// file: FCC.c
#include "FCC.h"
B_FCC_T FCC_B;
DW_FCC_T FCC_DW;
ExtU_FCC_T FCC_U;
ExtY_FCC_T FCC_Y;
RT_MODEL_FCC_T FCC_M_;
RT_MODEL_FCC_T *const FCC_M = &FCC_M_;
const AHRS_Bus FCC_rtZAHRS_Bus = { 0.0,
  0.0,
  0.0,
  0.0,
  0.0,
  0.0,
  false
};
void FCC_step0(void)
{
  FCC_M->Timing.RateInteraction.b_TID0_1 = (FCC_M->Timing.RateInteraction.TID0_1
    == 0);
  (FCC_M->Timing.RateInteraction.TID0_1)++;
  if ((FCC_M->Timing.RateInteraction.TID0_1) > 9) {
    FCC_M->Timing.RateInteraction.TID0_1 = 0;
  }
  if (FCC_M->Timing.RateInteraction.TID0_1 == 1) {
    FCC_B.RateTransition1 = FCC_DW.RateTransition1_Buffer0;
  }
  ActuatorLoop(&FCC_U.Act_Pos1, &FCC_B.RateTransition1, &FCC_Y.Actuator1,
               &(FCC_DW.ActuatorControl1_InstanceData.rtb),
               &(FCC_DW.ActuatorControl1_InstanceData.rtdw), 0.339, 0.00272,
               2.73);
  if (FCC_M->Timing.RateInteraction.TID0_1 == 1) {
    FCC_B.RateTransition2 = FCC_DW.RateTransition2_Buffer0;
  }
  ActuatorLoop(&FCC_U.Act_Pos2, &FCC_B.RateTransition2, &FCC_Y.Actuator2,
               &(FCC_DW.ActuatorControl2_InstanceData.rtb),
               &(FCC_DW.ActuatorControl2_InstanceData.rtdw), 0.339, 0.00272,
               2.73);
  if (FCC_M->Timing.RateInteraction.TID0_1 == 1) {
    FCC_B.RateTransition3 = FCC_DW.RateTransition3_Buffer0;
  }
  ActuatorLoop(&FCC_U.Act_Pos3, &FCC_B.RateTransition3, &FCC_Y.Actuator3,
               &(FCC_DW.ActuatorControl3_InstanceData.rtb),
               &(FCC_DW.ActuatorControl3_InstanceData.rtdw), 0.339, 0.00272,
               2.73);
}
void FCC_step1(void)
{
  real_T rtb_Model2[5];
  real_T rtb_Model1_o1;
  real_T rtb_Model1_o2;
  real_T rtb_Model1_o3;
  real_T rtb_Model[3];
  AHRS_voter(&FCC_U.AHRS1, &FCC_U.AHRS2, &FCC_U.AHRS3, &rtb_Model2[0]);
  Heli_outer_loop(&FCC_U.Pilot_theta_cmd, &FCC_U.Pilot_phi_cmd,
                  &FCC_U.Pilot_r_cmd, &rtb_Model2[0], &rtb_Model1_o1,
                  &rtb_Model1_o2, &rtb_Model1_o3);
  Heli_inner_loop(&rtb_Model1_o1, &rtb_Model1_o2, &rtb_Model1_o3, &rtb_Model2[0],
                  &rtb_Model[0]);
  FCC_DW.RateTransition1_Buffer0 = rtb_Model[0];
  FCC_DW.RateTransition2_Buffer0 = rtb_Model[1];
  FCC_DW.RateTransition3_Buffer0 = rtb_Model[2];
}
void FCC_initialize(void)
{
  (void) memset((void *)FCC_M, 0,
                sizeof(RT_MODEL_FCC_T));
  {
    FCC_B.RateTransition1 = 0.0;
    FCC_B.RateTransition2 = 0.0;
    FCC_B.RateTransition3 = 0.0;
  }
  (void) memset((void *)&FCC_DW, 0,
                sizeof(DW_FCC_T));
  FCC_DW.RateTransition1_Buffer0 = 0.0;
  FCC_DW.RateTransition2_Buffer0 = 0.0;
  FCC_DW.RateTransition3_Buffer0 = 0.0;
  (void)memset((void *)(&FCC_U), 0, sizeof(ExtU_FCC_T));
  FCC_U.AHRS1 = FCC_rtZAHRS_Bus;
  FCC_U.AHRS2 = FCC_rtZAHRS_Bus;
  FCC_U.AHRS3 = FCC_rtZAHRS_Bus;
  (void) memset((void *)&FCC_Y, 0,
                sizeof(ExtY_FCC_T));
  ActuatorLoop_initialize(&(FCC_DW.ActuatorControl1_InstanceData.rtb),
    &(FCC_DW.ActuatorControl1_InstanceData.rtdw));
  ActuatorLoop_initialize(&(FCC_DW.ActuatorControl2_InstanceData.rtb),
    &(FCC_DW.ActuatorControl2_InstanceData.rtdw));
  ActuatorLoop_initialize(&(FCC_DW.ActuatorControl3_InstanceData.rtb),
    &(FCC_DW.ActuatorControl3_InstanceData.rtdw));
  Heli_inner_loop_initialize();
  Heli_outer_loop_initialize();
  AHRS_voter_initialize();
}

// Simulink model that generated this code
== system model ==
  Act_Pos1 : Inport
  Act_Pos2 : Inport
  Act_Pos3 : Inport
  Pilot_theta_cmd : Inport
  Pilot_phi_cmd : Inport
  Pilot_r_cmd : Inport
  AHRS1 : Inport
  AHRS2 : Inport
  AHRS3 : Inport
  Actuator1 : Outport  <- 1: ActuatorControl1
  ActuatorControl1 : ModelReference  <- 1: Act_Pos1, 2: RateTransition1
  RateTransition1 : RateTransition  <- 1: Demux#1
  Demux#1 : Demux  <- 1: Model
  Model : ModelReference  <- 1: Model1, 2: Model1/2, 3: Model1/3, 4: Model2
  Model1 : ModelReference  <- 1: Pilot_theta_cmd, 2: Pilot_phi_cmd, 3: Pilot_r_cmd, 4: Model2
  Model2 : ModelReference  <- 1: AHRS1, 2: AHRS2, 3: AHRS3
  Actuator2 : Outport  <- 1: ActuatorControl2
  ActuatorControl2 : ModelReference  <- 1: Act_Pos2, 2: RateTransition2
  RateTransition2 : RateTransition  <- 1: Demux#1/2
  Actuator3 : Outport  <- 1: ActuatorControl3
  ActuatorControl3 : ModelReference  <- 1: Act_Pos3, 2: RateTransition3
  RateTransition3 : RateTransition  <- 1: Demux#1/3
